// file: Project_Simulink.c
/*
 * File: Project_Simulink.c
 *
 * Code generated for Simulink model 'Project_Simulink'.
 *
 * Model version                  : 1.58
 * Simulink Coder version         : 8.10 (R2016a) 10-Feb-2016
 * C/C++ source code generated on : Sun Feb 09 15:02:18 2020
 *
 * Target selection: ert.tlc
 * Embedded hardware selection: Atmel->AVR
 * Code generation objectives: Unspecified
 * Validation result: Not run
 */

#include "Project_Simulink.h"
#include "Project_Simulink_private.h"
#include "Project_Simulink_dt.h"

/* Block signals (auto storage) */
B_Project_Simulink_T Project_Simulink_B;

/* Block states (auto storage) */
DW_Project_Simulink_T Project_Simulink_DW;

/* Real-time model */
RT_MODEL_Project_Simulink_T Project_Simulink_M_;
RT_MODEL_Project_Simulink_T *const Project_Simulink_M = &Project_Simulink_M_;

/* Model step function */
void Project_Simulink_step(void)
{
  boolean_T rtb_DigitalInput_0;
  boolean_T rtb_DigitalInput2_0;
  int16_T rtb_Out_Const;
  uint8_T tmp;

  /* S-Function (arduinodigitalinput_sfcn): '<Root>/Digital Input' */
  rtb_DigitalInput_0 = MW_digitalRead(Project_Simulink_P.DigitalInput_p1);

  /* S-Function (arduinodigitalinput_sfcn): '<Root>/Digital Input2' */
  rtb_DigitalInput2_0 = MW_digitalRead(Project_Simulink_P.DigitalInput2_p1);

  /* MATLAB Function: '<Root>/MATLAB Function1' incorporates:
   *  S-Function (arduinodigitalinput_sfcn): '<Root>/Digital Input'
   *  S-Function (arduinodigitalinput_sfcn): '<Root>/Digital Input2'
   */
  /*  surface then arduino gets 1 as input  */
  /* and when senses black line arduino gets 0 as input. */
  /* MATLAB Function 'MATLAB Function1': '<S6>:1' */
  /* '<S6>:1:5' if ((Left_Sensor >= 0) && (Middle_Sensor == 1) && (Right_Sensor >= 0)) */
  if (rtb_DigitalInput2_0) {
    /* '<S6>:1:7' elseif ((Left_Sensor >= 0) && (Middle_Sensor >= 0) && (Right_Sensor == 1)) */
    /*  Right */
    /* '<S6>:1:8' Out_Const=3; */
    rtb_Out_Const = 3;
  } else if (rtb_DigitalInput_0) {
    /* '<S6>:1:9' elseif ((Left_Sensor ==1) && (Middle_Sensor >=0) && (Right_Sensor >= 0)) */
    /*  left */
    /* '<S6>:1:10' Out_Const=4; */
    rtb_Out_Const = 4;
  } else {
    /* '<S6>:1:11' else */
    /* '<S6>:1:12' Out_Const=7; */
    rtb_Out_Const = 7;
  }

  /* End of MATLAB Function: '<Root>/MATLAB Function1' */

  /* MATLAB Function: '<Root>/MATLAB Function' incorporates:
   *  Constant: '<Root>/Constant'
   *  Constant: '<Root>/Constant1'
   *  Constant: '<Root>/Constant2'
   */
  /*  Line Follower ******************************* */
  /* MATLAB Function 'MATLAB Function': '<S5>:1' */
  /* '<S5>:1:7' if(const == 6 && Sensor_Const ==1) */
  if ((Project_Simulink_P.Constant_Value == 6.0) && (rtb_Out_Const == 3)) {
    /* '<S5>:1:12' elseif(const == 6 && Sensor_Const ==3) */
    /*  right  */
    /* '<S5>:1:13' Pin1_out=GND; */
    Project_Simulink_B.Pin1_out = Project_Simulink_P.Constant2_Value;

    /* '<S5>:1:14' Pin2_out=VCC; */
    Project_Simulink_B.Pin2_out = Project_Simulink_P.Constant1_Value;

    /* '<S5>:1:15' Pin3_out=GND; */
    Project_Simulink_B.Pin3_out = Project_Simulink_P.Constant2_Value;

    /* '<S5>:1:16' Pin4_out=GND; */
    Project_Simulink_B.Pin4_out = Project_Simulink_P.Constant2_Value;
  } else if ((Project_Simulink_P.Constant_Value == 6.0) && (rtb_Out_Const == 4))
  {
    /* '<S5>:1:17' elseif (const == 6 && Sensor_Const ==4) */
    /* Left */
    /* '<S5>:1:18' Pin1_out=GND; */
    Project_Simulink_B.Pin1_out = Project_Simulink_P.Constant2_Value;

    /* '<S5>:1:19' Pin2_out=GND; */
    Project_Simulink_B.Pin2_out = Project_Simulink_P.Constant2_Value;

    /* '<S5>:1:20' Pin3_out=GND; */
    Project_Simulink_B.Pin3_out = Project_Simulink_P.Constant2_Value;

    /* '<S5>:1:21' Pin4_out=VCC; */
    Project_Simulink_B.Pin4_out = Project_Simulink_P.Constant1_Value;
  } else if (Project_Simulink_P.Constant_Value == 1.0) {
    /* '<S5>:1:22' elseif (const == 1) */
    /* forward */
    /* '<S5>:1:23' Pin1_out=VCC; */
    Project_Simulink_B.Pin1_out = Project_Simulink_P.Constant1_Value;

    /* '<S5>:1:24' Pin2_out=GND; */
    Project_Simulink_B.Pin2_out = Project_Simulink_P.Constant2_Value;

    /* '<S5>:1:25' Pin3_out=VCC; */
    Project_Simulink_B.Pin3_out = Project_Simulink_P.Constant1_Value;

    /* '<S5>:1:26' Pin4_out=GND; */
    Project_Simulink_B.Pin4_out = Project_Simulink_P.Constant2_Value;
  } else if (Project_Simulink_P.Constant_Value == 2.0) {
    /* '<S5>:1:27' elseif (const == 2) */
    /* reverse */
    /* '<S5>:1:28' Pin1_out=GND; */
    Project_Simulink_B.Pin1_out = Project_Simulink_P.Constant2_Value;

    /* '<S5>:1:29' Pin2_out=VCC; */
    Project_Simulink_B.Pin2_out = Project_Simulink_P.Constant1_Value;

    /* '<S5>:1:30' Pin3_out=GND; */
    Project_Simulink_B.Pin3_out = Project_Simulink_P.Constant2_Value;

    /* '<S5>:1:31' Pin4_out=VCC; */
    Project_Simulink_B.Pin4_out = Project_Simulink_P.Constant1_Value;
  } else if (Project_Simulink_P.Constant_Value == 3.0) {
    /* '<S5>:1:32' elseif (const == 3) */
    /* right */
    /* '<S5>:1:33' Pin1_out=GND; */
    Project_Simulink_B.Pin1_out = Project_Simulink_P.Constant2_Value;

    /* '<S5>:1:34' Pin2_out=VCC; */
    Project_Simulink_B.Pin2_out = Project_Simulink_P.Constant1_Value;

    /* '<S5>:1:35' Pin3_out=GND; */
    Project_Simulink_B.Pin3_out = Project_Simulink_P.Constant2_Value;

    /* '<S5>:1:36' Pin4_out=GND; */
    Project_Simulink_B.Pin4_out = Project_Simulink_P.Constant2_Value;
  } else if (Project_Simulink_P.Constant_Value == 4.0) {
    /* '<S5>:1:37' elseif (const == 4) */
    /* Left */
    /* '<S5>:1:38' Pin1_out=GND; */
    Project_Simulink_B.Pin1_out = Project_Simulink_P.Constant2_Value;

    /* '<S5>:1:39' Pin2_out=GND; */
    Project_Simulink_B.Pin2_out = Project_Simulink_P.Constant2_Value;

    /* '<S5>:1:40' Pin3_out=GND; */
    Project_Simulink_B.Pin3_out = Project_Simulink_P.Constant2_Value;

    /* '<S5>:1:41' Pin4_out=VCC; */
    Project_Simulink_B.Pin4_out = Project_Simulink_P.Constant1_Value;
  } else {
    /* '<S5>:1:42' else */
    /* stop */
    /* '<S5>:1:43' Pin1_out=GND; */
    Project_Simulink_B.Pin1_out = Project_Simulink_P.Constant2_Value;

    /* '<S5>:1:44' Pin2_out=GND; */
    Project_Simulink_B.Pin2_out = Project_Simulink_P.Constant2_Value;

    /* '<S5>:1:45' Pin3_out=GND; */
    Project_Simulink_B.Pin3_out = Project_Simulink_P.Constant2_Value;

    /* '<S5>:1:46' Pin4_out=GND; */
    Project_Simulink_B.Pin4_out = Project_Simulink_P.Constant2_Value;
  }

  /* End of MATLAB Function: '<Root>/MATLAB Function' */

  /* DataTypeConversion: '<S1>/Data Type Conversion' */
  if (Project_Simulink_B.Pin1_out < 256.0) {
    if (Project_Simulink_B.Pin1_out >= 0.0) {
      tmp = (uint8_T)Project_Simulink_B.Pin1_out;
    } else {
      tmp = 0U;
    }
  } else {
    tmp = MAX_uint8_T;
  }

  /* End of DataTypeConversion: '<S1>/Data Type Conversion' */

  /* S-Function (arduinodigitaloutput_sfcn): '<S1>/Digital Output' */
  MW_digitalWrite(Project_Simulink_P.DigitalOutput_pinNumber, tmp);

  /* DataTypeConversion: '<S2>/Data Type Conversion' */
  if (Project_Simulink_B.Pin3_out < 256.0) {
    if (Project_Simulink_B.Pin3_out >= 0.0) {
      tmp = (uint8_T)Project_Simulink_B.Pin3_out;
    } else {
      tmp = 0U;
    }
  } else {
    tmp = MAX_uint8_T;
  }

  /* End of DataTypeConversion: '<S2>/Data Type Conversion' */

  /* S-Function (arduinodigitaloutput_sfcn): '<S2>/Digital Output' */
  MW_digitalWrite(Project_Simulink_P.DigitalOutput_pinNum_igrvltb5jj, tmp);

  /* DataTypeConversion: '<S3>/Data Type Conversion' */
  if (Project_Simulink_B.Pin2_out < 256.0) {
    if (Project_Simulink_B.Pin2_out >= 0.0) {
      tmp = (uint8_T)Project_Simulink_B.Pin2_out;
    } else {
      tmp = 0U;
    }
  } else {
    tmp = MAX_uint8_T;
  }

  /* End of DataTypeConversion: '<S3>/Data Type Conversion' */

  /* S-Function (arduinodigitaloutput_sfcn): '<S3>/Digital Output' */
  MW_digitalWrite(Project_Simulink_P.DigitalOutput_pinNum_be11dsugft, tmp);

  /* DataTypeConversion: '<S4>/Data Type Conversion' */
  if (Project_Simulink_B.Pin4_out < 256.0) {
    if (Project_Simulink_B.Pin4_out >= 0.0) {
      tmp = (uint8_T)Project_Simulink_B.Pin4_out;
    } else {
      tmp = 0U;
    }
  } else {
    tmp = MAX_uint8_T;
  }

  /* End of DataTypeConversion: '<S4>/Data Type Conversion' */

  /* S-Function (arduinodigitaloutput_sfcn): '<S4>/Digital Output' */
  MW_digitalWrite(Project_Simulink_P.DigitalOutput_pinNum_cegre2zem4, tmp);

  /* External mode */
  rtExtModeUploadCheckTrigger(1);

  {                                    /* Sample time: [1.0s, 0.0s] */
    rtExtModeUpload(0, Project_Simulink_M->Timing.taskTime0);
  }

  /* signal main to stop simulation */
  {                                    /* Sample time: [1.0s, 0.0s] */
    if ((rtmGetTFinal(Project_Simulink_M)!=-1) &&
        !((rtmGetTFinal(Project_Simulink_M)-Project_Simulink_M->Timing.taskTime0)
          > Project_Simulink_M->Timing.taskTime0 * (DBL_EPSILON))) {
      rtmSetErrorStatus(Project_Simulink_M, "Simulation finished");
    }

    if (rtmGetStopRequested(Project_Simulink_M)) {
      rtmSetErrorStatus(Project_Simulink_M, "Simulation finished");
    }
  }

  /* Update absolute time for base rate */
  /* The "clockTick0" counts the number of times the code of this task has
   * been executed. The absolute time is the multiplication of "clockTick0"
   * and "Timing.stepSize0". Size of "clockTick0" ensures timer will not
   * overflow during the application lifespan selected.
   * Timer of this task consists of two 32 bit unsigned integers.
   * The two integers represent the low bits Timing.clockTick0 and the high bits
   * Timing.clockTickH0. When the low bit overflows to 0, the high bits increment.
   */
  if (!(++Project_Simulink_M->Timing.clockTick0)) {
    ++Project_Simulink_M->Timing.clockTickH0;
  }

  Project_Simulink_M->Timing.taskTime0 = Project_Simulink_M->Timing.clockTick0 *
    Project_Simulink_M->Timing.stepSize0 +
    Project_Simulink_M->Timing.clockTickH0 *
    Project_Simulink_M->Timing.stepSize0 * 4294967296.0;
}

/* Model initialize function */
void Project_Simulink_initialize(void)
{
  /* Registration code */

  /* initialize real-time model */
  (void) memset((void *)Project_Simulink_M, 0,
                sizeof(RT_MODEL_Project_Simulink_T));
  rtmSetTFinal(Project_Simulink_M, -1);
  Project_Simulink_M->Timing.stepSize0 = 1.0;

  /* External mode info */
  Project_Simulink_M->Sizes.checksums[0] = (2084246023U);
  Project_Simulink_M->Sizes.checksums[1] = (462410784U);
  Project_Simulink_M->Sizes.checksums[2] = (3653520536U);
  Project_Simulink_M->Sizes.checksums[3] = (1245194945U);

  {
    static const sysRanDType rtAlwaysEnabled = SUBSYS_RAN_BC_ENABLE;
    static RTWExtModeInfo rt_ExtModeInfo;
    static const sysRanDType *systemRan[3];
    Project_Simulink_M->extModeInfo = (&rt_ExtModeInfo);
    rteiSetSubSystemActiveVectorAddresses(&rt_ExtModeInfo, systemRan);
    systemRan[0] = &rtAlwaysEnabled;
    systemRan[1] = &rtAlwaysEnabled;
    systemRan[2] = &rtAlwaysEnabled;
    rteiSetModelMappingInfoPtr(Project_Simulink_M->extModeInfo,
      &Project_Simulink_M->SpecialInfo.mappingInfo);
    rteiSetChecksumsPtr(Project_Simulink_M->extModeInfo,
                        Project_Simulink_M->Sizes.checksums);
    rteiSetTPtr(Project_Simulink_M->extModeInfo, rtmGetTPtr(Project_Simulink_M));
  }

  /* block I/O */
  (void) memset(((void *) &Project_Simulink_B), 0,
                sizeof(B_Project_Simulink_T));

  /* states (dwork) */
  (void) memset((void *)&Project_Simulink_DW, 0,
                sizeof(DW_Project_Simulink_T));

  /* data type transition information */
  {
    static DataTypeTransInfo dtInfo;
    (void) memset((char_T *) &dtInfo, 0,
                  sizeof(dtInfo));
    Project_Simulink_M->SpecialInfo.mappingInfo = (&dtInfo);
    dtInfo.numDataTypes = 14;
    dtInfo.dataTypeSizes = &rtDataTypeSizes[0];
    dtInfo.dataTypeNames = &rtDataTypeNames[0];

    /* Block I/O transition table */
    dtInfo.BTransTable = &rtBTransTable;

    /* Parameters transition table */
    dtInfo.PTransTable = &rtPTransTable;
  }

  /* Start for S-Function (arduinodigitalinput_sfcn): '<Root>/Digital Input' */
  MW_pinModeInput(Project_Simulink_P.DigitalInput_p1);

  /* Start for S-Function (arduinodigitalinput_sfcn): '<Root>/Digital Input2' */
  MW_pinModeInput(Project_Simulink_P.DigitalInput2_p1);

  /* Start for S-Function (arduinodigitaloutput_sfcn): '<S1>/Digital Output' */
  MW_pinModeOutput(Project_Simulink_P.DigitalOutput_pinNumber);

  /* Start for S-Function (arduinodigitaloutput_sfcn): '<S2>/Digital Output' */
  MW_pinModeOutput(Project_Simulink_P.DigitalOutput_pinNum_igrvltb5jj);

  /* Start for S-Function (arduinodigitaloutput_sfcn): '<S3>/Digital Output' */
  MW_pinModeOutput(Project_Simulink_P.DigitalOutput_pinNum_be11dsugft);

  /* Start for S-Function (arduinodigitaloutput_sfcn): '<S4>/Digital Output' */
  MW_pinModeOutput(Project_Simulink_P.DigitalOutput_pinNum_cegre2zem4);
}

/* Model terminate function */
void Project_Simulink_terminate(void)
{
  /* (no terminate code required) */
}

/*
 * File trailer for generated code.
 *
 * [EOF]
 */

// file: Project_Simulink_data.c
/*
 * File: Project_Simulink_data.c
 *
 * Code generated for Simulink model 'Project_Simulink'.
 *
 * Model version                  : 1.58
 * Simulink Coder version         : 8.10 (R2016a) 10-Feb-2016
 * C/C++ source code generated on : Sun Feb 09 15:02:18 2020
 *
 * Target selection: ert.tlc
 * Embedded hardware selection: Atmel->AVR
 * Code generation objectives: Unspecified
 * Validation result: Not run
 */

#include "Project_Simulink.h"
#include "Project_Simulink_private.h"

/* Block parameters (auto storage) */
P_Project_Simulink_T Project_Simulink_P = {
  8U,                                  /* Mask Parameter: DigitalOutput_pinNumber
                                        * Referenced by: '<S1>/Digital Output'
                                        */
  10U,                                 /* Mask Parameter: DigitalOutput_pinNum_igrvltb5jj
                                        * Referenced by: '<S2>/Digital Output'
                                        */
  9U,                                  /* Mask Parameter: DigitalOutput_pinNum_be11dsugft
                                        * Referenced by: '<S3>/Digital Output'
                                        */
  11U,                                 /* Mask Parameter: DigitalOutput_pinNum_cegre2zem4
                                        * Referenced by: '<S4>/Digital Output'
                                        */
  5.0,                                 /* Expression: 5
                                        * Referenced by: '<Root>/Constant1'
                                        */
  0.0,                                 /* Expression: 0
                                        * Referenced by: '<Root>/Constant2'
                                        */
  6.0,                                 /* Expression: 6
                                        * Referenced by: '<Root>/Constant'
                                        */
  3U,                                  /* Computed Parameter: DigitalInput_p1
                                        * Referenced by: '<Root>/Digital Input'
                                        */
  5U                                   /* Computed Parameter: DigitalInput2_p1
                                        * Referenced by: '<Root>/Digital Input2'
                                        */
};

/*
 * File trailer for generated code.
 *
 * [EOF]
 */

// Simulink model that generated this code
simulink model "Project_Simulink"  (R2016a)
settings: Solver=FixedStepAuto  StartTime=0.0  StopTime=inf  RelTol=1e-3
libraries: arduinolib x6

== system Project_Simulink ==
  Constant : Constant  Value=6
  Constant1 : Constant  Value=5
  Constant2 : Constant  Value=0
  Digital Input : arduinolib/Digital Input  pinNumber=3  sampleTime=1  blockPlatform=arduino
  Digital Input2 : arduinolib/Digital Input  pinNumber=5  sampleTime=1  blockPlatform=arduino
  Digital Output : arduinolib/Digital Output  pinNumber=8  blockPlatform=arduino
  Digital Output1 : arduinolib/Digital Output  pinNumber=10  blockPlatform=arduino
  Digital Output2 : arduinolib/Digital Output  pinNumber=9  blockPlatform=arduino
  Digital Output3 : arduinolib/Digital Output  pinNumber=11  blockPlatform=arduino
  MATLAB Function : MATLAB Function  TreatAsAtomicUnit=on
  MATLAB Function1 : MATLAB Function  TreatAsAtomicUnit=on
  Scope : Scope  NumInputPorts=4
  wires:
  MATLAB Function/1(Pin1_out) -> Scope/1, Digital Output/1
  MATLAB Function/2(Pin2_out) -> Scope/2, Digital Output2/1
  MATLAB Function/3(Pin3_out) -> Scope/3, Digital Output1/1
  MATLAB Function/4(Pin4_out) -> Scope/4, Digital Output3/1
  Constant/1 -> MATLAB Function/3(const)
  Constant1/1 -> MATLAB Function/1(VCC)
  Constant2/1 -> MATLAB Function/2(GND)
  Digital Input2/1 -> MATLAB Function1/3(Right_Sensor)
  Digital Input/1 -> MATLAB Function1/1(Left_Sensor)
  MATLAB Function1/1(Out_Const) -> MATLAB Function/4(Sensor_Const)

== matlab function Project_Simulink/MATLAB Function1 ==
function Out_Const  = fcn(Left_Sensor,Middle_Sensor,Right_Sensor)
%#codegen
% surface then arduino gets 1 as input 
%and when senses black line arduino gets 0 as input.
if ((Left_Sensor >= 0) && (Middle_Sensor == 1) && (Right_Sensor >= 0)) % forward
    Out_Const=1;
elseif ((Left_Sensor >= 0) && (Middle_Sensor >= 0) && (Right_Sensor == 1)) % Right
    Out_Const=3;
elseif ((Left_Sensor ==1) && (Middle_Sensor >=0) && (Right_Sensor >= 0)) % left
    Out_Const=4;  
else
    Out_Const=7;  
    
end

== matlab function Project_Simulink/MATLAB Function ==

function [Pin1_out,Pin2_out,Pin3_out,Pin4_out] = fcn(VCC,GND,const,Sensor_Const)

% Line Follower *******************************

if(const == 6 && Sensor_Const ==1) % forward
    Pin1_out=VCC;
    Pin2_out=GND;
    Pin3_out=VCC;
    Pin4_out=GND;
elseif(const == 6 && Sensor_Const ==3) % right 
    Pin1_out=GND;
    Pin2_out=VCC;
    Pin3_out=GND;
    Pin4_out=GND;
elseif (const == 6 && Sensor_Const ==4) %Left
    Pin1_out=GND;
    Pin2_out=GND;
    Pin3_out=GND;
    Pin4_out=VCC;    
elseif (const == 1) %forward
    Pin1_out=VCC;
    Pin2_out=GND;
    Pin3_out=VCC;
    Pin4_out=GND;
elseif (const == 2) %reverse
    Pin1_out=GND;
    Pin2_out=VCC;
    Pin3_out=GND;
    Pin4_out=VCC;
elseif (const == 3) %right
    Pin1_out=GND;
    Pin2_out=VCC;
    Pin3_out=GND;
    Pin4_out=GND;
elseif (const == 4) %Left
    Pin1_out=GND;
    Pin2_out=GND;
    Pin3_out=GND;
    Pin4_out=VCC;
else    %stop
    Pin1_out=GND;
    Pin2_out=GND;
    Pin3_out=GND;
    Pin4_out=GND;

end
